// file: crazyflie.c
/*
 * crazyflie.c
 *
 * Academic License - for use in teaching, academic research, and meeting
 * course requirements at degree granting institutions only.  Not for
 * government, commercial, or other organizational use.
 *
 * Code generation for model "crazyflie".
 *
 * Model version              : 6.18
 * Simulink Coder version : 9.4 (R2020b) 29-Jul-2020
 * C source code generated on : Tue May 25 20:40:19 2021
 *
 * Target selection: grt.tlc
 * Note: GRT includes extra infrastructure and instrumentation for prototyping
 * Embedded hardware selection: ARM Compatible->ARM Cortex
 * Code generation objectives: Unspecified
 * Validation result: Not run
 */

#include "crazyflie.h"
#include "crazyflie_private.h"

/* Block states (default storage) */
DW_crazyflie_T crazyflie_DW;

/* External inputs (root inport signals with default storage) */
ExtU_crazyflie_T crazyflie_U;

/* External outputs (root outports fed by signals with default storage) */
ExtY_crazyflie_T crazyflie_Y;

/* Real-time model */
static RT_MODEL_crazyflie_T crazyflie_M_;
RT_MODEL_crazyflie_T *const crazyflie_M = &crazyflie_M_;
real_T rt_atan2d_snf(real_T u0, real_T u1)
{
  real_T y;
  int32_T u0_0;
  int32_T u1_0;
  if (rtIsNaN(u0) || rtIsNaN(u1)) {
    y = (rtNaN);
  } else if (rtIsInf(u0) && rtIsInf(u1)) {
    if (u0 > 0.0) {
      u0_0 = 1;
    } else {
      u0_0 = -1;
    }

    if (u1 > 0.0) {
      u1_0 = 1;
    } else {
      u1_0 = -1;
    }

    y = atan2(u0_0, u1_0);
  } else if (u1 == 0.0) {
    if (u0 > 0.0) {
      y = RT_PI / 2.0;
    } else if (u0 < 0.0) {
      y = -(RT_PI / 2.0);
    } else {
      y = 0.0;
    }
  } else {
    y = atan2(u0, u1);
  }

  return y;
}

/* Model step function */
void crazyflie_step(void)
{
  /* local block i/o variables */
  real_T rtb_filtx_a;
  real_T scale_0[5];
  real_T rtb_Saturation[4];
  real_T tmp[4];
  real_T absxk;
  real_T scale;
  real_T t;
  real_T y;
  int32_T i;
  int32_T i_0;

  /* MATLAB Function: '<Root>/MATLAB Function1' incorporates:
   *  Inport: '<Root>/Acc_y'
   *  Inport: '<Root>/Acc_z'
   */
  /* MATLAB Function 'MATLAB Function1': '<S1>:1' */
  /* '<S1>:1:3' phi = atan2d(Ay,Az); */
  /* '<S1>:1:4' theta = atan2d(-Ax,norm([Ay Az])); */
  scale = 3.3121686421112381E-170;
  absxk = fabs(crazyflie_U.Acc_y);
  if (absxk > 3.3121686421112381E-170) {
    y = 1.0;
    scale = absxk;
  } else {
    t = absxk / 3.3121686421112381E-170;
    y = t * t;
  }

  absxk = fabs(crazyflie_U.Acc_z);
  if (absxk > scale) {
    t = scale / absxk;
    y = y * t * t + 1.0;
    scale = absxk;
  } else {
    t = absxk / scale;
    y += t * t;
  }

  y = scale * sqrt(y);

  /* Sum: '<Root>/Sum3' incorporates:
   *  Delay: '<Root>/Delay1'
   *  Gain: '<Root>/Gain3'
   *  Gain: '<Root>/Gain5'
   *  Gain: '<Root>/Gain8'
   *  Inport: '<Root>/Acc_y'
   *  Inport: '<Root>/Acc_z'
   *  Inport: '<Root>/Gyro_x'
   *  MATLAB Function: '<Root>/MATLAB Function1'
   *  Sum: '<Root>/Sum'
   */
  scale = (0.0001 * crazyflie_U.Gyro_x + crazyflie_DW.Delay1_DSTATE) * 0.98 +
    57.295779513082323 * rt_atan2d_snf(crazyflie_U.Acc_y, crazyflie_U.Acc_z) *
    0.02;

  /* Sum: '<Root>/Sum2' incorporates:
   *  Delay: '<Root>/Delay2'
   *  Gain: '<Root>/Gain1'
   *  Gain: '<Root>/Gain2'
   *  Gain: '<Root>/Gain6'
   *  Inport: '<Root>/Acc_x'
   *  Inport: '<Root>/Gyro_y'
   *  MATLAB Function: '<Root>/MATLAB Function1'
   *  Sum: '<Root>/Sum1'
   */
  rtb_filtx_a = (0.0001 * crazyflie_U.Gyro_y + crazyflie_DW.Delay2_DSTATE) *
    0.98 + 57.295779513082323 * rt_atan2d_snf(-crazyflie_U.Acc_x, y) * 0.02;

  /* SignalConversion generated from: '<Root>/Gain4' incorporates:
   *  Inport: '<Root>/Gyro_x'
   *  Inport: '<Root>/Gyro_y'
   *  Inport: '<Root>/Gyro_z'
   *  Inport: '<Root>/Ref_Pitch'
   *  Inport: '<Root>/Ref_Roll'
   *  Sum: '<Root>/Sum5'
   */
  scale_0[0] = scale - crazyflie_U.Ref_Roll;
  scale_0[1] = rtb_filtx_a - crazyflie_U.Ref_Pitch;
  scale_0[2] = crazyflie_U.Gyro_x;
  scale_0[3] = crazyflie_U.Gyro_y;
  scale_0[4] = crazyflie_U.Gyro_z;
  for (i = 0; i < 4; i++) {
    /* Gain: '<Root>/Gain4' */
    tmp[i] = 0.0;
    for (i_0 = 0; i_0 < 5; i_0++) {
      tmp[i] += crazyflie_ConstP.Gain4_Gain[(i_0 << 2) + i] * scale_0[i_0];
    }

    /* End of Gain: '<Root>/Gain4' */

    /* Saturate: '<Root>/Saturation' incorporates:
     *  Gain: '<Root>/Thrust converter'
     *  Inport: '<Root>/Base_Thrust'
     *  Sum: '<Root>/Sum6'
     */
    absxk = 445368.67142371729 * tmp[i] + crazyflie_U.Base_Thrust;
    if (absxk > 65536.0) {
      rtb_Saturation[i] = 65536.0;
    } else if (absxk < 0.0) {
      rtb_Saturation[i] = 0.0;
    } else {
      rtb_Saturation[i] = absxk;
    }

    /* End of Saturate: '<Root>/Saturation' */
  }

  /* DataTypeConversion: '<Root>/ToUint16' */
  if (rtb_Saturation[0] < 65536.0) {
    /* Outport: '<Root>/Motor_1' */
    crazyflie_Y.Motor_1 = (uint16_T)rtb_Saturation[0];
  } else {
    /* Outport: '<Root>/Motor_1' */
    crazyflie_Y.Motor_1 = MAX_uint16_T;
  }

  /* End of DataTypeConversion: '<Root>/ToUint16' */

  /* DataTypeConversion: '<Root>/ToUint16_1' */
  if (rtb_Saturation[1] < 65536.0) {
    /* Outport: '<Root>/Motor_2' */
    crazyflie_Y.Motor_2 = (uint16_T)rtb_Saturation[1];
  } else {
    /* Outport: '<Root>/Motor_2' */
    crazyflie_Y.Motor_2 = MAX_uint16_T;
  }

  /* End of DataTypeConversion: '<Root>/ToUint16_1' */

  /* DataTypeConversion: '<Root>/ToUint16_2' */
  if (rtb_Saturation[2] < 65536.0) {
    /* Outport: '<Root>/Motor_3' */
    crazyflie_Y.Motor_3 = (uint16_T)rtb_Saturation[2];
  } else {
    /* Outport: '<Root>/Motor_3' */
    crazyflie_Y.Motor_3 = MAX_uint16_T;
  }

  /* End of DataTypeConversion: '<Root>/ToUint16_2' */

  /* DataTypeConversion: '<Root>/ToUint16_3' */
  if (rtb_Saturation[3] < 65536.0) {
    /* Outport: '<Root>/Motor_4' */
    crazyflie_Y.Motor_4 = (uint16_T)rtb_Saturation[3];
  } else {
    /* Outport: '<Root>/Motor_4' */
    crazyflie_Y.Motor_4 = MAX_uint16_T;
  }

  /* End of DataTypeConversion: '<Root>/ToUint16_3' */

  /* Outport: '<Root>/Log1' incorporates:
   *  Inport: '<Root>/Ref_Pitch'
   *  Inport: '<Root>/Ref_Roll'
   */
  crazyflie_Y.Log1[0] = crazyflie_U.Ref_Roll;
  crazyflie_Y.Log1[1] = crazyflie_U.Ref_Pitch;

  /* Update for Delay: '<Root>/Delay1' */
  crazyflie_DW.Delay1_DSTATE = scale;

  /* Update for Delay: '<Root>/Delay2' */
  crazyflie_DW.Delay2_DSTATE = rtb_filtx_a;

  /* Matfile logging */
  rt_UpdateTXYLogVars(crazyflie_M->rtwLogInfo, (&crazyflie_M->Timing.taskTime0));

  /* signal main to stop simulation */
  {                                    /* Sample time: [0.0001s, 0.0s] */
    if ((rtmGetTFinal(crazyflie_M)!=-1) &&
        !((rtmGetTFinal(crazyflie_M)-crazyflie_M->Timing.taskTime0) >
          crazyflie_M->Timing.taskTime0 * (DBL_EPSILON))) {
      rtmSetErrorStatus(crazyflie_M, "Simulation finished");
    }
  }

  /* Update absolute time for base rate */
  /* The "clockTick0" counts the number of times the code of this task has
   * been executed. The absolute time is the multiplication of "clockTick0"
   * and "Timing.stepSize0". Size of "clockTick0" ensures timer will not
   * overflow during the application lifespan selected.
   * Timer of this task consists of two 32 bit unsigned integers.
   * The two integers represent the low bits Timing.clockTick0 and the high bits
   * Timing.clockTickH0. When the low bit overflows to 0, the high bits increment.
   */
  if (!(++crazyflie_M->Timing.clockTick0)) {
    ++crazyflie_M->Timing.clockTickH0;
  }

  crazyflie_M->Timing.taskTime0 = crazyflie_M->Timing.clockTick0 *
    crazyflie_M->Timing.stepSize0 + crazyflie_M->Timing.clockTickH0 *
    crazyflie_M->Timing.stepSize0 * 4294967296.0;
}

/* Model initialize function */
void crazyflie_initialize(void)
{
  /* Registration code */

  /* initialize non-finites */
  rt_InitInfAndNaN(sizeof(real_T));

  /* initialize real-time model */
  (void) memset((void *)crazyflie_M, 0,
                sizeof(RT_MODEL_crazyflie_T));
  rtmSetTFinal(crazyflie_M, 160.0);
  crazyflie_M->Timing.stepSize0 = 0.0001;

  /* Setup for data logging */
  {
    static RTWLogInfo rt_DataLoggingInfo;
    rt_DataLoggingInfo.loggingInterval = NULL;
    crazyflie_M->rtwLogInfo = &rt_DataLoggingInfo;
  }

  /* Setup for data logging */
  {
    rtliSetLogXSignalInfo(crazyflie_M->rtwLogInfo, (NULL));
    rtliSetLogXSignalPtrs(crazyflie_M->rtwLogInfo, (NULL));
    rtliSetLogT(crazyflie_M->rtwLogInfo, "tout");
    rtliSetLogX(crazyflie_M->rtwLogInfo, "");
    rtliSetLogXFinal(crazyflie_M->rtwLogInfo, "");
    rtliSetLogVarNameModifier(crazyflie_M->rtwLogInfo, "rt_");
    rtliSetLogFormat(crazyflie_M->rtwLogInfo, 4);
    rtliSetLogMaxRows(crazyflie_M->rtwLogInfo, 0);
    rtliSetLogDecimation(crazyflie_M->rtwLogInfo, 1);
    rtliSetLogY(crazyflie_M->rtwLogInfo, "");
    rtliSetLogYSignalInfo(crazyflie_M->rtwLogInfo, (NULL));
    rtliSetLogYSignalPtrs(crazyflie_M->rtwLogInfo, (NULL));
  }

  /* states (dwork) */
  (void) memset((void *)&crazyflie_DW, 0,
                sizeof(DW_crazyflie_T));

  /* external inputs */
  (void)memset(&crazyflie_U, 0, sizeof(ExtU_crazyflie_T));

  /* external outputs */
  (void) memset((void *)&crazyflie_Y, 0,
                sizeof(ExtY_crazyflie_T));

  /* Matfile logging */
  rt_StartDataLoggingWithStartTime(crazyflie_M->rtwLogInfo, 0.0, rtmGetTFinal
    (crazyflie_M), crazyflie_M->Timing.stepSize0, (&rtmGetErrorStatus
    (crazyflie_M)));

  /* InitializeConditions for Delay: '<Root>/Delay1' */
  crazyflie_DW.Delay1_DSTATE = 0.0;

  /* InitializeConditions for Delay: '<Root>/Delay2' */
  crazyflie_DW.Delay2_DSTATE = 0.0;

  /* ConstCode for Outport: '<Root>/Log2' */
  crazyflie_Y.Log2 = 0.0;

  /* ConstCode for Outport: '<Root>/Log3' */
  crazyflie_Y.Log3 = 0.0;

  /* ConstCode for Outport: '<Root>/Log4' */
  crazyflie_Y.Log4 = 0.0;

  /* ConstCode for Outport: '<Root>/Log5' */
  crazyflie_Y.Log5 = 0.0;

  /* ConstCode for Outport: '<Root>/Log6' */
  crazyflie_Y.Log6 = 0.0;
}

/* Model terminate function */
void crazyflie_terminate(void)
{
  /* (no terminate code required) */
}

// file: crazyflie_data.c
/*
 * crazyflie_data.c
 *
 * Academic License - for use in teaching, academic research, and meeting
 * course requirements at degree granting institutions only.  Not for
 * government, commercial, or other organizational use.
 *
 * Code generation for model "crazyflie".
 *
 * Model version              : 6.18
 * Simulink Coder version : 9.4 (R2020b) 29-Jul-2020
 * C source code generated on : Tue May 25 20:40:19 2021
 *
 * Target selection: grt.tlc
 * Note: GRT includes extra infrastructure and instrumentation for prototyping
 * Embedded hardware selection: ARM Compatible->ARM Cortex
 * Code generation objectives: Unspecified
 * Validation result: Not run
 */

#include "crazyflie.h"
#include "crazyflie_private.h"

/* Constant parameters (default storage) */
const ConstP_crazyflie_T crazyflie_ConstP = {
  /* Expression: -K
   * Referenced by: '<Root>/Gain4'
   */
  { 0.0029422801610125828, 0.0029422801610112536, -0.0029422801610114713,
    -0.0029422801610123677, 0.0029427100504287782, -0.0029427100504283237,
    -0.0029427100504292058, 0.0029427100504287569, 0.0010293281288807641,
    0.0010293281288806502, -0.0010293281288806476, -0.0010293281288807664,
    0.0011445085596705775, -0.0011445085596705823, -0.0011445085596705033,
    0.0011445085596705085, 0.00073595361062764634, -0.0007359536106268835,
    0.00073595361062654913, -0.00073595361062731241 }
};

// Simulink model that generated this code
simulink model "crazyflie"  (R2020b)
settings: Solver=FixedStepDiscrete  StartTime=0.0  StopTime=160  FixedStep=0.0001  RelTol=1e-3
values from neighbouring files (symbols this model uses):
  g = 9.81    [linearized_states.m]
  Ts = 0.0001    [linearized_states.m]
undefined symbols (not defined in the file or in its folder): K

== system crazyflie ==
  note: 65536 <==> 60 grams
  note: Logging
  note: Outputs
  note: Controller input
  note: Ref_Roll: +/- 25 deg
  note: Base_Thrust: 0 - 65536
  note: Ref_Pitch: +/- 25 deg
  note: Ref_YawRate: +/- 100 deg/s
  note: Controller input ranges:
  note: Gyroscope:
      | Angular velocity [degree / s]
  note: Accelerometer:
      | Acceleration [m/s^2/g]
  note: Sensor data units:
  note: Flowdeck data
  note: Sensor data
  note: Sensor data from
      | workspace
  Base_Thrust : Inport  OutDataTypeStr=double
  Ref_Roll : Inport  Port=2  OutDataTypeStr=double
  Ref_Pitch : Inport  Port=3  OutDataTypeStr=double
  Ref_YawRate : Inport  Port=4  OutDataTypeStr=double
  Flow_x : Inport  Port=5  OutDataTypeStr=int16  PortDimensions=1
  Flow_y : Inport  Port=6  OutDataTypeStr=int16  PortDimensions=1
  Acc_x : Inport  Port=7  OutDataTypeStr=double  PortDimensions=1
  Acc_y : Inport  Port=8  OutDataTypeStr=double  PortDimensions=1
  Acc_z : Inport  Port=9  OutDataTypeStr=double  PortDimensions=1
  Gyro_x : Inport  Port=10  OutDataTypeStr=double  PortDimensions=1
  Gyro_y : Inport  Port=11  OutDataTypeStr=double  PortDimensions=1
  Gyro_z : Inport  Port=12  OutDataTypeStr=double  PortDimensions=1
  Delay1 : Delay  DelayLength=1  InitialCondition=0
  Delay2 : Delay  DelayLength=1  InitialCondition=0
  Demux : Demux
  From Workspace : FromWorkspace  VariableName=Acc_x  OutDataTypeStr=double
  From Workspace1 : FromWorkspace  VariableName=Acc_y  OutDataTypeStr=double
  From Workspace2 : FromWorkspace  VariableName=Acc_z  OutDataTypeStr=double
  From Workspace3 : FromWorkspace  VariableName=Gyro_x  OutDataTypeStr=double
  From Workspace4 : FromWorkspace  VariableName=Gyro_y  OutDataTypeStr=double
  From Workspace5 : FromWorkspace  VariableName=Gyro_z  OutDataTypeStr=double
  Gain1 : Gain  Gain=0.98
  Gain2 : Gain  Gain=0.02
  Gain3 : Gain  Gain=0.02
  Gain4 : Gain  Gain=-K  Multiplication=Matrix(K*u)
  Gain5 : Gain  Gain=Ts
  Gain6 : Gain  Gain=Ts
  Gain8 : Gain  Gain=0.98
  MATLAB Function1 : MATLAB Function  TreatAsAtomicUnit=on
  Mux : Mux  Inputs=2
  Mux1 : Mux  Inputs=3
  Mux2 : Mux  Inputs=2
  Mux3 : Mux  Inputs=2
  Saturation : Saturate  UpperLimit=65536  LowerLimit=0
  Scope : Scope
  Sum : Sum  Inputs=|++
  Sum1 : Sum  Inputs=|++
  Sum2 : Sum  Inputs=++|
  Sum3 : Sum  Inputs=++|
  Sum5 : Sum  Inputs=|-+
  Sum6 : Sum  Inputs=++|
  Thrust converter : Gain  Gain=(4*65536)/(0.06*g)
  ToDouble{,1..5} (6 alike) : DataTypeConversion  OutDataTypeStr=double  SaturateOnIntegerOverflow=on
  ToUint16 : DataTypeConversion  OutDataTypeStr=uint16  SaturateOnIntegerOverflow=on
  ToUint16_1 : DataTypeConversion  OutDataTypeStr=uint16  SaturateOnIntegerOverflow=on
  ToUint16_2 : DataTypeConversion  OutDataTypeStr=uint16  SaturateOnIntegerOverflow=on
  ToUint16_3 : DataTypeConversion  OutDataTypeStr=uint16  SaturateOnIntegerOverflow=on
  Motor_1 : Outport  OutDataTypeStr=uint16  VectorParamsAs1DForOutWhenUnconnected=off  LockScale=on
  Motor_2 : Outport  Port=2  OutDataTypeStr=uint16  VectorParamsAs1DForOutWhenUnconnected=off  LockScale=on
  Motor_3 : Outport  Port=3  OutDataTypeStr=uint16  VectorParamsAs1DForOutWhenUnconnected=off  LockScale=on
  Motor_4 : Outport  Port=4  OutDataTypeStr=uint16  VectorParamsAs1DForOutWhenUnconnected=off  LockScale=on
  Log1 : Outport  Port=5  OutDataTypeStr=double  VectorParamsAs1DForOutWhenUnconnected=off
  Log2 : Outport  Port=6  OutDataTypeStr=double  VectorParamsAs1DForOutWhenUnconnected=off
  Log3 : Outport  Port=7  OutDataTypeStr=double  VectorParamsAs1DForOutWhenUnconnected=off
  Log4 : Outport  Port=8  OutDataTypeStr=double  VectorParamsAs1DForOutWhenUnconnected=off
  Log5 : Outport  Port=9  OutDataTypeStr=double  VectorParamsAs1DForOutWhenUnconnected=off
  Log6 : Outport  Port=10  OutDataTypeStr=double  VectorParamsAs1DForOutWhenUnconnected=off
  wires:
  ToUint16/1 -> Motor_1/1
  ToUint16_1/1 -> Motor_2/1
  ToUint16_2/1 -> Motor_3/1
  ToUint16_3/1 -> Motor_4/1
  ToDouble/1 -> Log1/1
  ToDouble1/1 -> Log2/1
  ToDouble2/1 -> Log3/1
  ToDouble3/1 -> Log4/1
  ToDouble4/1 -> Log5/1
  ToDouble5/1 -> Log6/1
  Gain5/1 -> Sum/1
  Delay1/1 -> Sum/2
  Gain8/1 -> Sum3/2
  Sum/1 -> Gain8/1
  Acc_x/1 -> MATLAB Function1/1(Ax)
  Acc_z/1 -> MATLAB Function1/3(Az)
  Gyro_x/1 -> Mux1/1, Gain5/1
  Gyro_y/1 -> Mux1/2, Gain6/1
  Gain3/1 -> Sum3/1
  Sum3/1 -> Delay1/1, Mux/1  "filt x"
  Sum1/1 -> Gain1/1
  Gain1/1 -> Sum2/2
  Delay2/1 -> Sum1/2
  Gain6/1 -> Sum1/1
  Sum2/1 -> Scope/1, Mux/2, Delay2/1  "filt x"
  Gain2/1 -> Sum2/1
  Mux1/1 -> [Angular_v]
  Gyro_z/1 -> Mux1/3
  Ref_Roll/1 -> Mux2/1
  Ref_Pitch/1 -> Mux2/2
  Mux/1 -> Sum5/2
  Sum5/1 -> Mux3/1
  [Angular_v] -> Mux3/2
  Mux3/1 -> Gain4/1
  Sum6/1 -> Saturation/1
  Saturation/1 -> Demux/1
  Demux/2 -> ToUint16_1/1
  Demux/3 -> ToUint16_2/1
  Demux/4 -> ToUint16_3/1
  Demux/1 -> ToUint16/1
  Acc_y/1 -> MATLAB Function1/2(Ay)
  MATLAB Function1/2(theta) -> Gain2/1
  MATLAB Function1/1(phi) -> Gain3/1
  Mux2/1 -> ToDouble/1, Sum5/1
  Gain4/1 -> Thrust converter/1
  Base_Thrust/1 -> Sum6/1
  Thrust converter/1 -> Sum6/2

== matlab function crazyflie/MATLAB Function1 ==
function [phi, theta] = fcn(Ax,Ay,Az)
    
phi = atan2d(Ay,Az);
theta = atan2d(-Ax,norm([Ay Az]));
end
